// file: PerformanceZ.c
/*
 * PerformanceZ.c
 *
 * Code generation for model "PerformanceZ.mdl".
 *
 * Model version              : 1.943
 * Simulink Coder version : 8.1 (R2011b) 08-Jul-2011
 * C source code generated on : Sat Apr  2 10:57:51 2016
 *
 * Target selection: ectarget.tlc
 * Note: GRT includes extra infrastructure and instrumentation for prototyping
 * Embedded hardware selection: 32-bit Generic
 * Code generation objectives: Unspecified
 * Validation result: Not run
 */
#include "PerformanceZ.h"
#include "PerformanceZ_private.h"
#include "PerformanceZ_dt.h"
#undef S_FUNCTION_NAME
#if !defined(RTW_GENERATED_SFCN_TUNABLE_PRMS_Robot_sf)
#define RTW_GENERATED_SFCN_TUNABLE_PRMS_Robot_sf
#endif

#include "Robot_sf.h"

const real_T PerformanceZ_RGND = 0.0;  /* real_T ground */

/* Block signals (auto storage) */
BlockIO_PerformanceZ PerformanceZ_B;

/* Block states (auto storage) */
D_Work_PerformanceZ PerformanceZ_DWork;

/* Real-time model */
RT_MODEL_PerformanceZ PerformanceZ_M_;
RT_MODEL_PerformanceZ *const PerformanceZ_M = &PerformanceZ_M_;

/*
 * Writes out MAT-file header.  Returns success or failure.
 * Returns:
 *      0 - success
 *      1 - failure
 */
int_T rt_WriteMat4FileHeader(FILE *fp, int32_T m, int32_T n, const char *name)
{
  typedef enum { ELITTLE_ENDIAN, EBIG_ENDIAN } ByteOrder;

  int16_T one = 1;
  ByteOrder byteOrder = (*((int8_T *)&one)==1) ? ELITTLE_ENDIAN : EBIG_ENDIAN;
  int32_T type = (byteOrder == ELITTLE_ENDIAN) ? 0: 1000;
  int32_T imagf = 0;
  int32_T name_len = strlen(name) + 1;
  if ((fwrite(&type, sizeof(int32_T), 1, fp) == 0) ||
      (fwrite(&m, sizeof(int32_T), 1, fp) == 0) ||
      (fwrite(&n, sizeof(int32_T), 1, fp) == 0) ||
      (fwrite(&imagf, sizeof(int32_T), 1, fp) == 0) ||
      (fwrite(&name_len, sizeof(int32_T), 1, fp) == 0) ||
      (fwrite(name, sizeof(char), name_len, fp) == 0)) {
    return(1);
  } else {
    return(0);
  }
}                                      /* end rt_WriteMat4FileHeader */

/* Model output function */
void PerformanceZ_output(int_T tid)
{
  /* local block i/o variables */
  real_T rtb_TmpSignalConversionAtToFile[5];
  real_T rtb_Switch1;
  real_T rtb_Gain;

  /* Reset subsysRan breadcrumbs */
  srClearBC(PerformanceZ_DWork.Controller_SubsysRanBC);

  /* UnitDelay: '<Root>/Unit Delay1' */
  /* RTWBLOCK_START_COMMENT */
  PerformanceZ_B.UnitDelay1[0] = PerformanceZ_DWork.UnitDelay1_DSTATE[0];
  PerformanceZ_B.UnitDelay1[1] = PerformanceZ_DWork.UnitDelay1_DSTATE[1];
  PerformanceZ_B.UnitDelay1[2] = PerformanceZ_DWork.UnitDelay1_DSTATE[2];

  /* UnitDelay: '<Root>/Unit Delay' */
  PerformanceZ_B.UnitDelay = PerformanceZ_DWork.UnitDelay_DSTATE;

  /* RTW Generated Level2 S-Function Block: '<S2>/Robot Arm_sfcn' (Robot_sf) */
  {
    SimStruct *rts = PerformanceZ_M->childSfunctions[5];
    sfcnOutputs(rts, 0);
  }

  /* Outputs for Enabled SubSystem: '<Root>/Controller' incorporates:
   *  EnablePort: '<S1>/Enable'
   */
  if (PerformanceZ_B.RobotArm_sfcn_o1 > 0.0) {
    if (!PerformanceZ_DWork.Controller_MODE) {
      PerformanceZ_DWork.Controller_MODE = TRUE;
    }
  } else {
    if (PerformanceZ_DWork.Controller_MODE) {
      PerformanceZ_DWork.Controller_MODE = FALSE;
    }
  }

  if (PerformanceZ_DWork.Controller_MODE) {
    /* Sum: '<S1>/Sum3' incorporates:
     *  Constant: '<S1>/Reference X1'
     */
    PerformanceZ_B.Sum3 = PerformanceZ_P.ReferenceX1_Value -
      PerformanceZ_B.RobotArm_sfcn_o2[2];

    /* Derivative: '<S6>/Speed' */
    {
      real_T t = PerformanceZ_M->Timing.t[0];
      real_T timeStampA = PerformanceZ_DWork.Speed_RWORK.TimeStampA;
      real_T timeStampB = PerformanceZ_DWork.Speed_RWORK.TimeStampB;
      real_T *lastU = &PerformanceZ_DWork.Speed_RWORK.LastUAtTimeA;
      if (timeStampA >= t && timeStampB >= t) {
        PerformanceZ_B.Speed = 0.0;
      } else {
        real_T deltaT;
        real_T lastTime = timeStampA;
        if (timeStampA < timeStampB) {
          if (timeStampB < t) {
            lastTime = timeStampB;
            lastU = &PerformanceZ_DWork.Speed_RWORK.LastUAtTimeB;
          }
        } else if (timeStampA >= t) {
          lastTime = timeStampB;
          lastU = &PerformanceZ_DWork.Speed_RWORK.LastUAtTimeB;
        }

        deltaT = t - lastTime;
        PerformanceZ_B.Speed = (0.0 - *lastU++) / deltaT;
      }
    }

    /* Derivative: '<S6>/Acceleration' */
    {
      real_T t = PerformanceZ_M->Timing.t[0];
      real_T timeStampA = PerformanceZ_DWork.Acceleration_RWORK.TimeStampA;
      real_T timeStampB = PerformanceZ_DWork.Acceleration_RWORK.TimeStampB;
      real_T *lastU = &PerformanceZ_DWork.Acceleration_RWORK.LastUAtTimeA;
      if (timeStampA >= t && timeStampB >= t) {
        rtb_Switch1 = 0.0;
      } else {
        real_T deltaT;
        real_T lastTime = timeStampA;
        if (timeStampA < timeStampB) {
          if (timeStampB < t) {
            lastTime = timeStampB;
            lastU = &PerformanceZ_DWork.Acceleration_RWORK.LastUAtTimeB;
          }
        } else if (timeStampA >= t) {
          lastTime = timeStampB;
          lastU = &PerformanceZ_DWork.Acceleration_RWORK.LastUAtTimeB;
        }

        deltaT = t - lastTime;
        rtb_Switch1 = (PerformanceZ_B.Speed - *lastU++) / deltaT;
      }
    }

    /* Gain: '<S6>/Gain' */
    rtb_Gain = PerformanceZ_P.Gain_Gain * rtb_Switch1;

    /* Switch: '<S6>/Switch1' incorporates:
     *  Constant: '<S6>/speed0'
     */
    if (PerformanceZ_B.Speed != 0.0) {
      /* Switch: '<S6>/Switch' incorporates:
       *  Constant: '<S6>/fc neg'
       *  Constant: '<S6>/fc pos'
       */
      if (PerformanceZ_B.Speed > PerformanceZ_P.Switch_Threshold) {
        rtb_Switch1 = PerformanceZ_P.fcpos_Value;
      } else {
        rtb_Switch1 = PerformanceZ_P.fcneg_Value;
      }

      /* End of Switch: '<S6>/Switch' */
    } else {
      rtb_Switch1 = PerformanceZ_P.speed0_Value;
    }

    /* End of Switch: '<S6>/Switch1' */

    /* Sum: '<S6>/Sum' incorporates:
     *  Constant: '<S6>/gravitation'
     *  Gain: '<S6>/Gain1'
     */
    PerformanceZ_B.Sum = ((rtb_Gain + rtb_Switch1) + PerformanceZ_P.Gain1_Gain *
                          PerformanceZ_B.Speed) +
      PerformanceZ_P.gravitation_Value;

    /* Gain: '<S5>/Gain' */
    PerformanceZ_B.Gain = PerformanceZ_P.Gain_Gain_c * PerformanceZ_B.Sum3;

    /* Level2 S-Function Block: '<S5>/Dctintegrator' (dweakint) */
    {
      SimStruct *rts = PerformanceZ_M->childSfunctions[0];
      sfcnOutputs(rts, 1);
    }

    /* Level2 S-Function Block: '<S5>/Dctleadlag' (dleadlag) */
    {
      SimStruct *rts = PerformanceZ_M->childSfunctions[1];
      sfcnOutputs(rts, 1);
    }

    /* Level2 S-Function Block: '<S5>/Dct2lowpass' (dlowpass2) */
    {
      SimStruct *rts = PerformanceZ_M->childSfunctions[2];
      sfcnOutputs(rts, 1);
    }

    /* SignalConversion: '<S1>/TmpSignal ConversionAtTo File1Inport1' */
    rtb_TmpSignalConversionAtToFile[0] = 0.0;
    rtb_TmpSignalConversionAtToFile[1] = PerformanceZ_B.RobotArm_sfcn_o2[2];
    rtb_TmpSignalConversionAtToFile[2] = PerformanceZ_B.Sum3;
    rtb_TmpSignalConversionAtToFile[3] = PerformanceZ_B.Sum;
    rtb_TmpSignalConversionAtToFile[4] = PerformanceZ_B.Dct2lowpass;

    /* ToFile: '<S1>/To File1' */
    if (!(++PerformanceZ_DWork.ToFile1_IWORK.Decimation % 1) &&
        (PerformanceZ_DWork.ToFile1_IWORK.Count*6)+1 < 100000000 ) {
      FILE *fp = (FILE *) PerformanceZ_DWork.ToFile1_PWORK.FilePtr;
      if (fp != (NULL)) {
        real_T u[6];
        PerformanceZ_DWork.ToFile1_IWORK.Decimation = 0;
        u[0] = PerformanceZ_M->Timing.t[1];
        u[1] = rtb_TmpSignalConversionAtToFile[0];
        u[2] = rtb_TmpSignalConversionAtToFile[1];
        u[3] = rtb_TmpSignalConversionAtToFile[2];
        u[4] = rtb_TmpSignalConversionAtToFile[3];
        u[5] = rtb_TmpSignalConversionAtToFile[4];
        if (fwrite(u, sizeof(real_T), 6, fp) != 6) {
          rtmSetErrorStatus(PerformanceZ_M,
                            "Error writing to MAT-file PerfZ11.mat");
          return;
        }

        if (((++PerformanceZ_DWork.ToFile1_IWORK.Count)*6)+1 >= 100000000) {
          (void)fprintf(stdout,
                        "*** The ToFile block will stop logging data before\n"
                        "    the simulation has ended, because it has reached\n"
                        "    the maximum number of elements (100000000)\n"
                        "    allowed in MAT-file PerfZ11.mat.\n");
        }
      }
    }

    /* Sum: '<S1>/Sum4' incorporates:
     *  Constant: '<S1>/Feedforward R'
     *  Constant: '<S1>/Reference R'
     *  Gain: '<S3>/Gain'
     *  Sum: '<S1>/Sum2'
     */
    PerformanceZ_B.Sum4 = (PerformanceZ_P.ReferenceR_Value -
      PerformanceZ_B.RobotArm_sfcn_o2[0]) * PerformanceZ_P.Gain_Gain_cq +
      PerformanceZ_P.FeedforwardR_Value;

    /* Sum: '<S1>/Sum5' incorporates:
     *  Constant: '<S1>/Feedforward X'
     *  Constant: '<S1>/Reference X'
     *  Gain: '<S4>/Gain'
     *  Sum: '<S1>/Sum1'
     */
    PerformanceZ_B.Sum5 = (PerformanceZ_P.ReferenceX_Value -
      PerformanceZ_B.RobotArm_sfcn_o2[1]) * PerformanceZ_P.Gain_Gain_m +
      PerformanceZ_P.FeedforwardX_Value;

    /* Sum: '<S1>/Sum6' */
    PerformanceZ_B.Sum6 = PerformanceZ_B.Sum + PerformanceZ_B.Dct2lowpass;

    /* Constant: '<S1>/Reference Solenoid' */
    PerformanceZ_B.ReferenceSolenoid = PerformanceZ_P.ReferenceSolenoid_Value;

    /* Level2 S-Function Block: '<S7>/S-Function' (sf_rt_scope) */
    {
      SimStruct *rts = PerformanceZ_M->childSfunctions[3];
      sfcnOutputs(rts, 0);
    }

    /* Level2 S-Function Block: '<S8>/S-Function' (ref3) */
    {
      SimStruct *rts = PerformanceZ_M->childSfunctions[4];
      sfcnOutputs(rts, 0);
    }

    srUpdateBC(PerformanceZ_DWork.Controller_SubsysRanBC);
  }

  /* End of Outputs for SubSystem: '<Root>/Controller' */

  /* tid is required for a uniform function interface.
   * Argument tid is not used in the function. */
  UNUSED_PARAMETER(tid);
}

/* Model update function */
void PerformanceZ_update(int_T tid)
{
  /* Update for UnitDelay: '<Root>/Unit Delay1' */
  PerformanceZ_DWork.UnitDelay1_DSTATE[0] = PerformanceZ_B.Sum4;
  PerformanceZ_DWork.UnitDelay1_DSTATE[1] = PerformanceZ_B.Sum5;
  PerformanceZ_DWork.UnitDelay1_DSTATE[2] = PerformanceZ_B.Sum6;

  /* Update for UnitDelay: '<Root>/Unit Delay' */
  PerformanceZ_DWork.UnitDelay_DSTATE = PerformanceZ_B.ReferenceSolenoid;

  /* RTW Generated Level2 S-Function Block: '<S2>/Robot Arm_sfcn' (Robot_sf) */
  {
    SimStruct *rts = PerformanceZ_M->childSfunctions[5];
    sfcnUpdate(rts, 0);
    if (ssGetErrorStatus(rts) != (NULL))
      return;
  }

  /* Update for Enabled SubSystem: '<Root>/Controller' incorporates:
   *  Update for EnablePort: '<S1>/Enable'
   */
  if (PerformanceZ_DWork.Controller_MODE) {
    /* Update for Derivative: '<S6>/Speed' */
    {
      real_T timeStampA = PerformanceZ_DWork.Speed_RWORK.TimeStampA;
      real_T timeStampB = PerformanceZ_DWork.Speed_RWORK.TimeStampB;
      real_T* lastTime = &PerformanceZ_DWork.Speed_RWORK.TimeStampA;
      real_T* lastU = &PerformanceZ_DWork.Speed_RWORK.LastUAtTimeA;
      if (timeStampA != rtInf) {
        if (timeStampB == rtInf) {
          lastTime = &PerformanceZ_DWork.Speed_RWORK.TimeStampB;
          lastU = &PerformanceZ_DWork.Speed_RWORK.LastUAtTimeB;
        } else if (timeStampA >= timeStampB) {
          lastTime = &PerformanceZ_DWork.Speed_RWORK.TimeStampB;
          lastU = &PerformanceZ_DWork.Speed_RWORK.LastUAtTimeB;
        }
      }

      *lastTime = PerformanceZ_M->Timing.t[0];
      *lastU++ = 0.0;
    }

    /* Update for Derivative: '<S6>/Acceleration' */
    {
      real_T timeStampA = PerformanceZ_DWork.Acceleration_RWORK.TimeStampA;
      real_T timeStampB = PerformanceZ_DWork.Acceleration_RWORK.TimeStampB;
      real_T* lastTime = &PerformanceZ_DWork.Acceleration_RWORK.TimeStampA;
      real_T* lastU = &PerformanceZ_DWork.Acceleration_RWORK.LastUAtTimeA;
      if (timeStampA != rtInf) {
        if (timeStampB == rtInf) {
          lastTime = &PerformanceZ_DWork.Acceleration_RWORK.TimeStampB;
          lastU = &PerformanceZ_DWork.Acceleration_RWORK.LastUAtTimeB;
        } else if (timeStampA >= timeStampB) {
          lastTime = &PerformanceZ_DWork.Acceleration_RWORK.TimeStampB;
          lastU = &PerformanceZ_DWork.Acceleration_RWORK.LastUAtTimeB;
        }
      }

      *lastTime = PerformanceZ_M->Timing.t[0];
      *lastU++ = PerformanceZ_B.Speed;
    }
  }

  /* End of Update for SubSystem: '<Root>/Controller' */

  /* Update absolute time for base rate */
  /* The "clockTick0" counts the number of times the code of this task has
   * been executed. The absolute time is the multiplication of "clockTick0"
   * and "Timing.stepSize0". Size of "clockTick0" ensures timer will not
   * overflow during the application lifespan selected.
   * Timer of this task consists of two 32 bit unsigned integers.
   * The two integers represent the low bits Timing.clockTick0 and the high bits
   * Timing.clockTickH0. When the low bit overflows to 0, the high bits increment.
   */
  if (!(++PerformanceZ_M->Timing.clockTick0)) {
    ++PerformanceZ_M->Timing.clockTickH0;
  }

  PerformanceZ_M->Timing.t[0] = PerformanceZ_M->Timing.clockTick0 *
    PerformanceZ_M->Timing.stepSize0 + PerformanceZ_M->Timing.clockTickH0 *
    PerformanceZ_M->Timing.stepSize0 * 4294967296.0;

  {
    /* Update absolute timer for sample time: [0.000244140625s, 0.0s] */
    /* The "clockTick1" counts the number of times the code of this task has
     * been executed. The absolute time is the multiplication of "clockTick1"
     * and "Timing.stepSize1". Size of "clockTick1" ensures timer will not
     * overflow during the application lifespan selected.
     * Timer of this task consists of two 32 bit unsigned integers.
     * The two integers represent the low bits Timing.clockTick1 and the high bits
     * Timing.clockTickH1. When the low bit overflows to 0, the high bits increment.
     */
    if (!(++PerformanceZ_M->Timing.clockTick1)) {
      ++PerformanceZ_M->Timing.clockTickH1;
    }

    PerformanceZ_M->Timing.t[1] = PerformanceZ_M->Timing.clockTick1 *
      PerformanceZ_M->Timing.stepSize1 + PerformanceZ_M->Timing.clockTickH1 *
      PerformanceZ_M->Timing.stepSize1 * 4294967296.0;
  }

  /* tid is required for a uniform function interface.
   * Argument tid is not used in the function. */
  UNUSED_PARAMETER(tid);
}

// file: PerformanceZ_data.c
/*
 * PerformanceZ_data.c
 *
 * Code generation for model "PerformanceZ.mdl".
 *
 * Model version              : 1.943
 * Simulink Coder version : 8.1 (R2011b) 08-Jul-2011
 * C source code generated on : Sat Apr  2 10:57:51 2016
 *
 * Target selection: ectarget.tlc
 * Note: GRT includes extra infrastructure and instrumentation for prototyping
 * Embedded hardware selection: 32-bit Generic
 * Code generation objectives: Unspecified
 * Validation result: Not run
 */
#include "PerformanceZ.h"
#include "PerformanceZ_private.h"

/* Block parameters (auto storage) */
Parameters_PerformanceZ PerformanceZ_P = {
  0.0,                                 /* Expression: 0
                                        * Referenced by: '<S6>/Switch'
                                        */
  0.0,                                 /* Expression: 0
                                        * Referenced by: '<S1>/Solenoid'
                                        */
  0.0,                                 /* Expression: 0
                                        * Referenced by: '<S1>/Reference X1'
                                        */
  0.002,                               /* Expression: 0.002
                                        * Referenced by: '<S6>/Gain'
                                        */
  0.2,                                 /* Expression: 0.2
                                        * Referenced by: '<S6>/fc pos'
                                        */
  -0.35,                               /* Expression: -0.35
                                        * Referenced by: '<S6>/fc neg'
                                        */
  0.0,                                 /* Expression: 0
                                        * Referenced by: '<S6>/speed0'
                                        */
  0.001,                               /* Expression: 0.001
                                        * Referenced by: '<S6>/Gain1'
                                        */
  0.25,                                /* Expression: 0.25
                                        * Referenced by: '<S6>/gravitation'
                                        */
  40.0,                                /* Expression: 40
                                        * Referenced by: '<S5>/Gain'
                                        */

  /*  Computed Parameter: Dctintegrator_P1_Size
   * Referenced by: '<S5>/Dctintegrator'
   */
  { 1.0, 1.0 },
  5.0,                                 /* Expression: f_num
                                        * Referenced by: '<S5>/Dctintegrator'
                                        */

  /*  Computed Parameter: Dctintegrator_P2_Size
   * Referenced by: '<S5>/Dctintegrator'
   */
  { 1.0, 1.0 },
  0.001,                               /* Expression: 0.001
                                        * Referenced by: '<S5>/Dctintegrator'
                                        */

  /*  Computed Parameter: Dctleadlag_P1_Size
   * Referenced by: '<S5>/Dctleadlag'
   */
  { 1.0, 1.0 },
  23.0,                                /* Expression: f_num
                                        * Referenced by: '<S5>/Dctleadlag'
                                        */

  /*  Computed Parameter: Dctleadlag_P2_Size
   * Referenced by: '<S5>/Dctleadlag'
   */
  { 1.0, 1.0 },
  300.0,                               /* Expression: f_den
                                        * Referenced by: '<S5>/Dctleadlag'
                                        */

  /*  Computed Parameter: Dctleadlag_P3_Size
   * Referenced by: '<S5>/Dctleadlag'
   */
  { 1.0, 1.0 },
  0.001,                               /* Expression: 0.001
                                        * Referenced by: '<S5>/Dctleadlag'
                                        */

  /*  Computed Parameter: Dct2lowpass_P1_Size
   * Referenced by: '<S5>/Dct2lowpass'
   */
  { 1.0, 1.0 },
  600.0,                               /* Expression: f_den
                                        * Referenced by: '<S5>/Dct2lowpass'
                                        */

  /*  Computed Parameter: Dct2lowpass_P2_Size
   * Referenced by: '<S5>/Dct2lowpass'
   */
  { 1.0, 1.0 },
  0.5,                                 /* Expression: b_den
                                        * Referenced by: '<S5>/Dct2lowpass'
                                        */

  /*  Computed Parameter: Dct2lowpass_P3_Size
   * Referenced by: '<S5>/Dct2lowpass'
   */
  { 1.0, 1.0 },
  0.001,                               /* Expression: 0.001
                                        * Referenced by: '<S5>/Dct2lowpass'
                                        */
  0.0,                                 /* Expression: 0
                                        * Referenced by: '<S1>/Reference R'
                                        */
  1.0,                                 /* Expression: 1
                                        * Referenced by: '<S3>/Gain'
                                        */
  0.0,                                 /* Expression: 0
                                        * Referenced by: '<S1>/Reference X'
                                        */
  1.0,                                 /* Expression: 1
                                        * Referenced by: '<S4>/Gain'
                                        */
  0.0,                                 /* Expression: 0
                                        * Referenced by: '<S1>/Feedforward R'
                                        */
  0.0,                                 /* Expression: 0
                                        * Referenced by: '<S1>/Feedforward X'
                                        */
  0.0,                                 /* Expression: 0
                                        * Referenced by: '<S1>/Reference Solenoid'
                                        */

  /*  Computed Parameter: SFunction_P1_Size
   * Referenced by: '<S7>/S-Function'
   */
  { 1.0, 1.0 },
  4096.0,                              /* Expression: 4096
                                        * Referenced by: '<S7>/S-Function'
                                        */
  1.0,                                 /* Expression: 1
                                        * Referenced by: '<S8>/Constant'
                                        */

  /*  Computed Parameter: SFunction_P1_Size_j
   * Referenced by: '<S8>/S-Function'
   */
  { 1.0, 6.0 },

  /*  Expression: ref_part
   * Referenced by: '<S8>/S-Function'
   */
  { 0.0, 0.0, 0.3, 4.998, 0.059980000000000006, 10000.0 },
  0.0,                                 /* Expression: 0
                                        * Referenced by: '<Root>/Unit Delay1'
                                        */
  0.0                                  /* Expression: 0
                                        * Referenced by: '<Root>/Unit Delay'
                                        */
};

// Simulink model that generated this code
simulink model "PerformanceZ"  (Simulink 7.8)
settings: Solver=FixedStepDiscrete  StartTime=0.0  StopTime=20  FixedStep=1/(1024*4)  RelTol=1e-3

== system PerformanceZ ==
  Accelerometer : Display
  Controller : Subsystem
  Robot Arm : Subsystem
  Unit Delay : UnitDelay  SampleTime=-1
  Unit Delay1 : UnitDelay  SampleTime=-1
  time1 : Display
  wires:
  Controller/1(Output) -> Unit Delay1/1
  Robot Arm/1(Homing Busy) -> Controller/Enable
  Robot Arm/2(Angle measurments [rad]) -> Controller/1(Angle Measurements [rad])
  Robot Arm/3(Airbag Status) -> time1/1
  Robot Arm/4(Accelerometer [V]) -> Accelerometer/1
  Controller/2(Solenoid) -> Unit Delay/1
  Unit Delay/1 -> Robot Arm/2(Solenoid)
  Unit Delay1/1 -> Robot Arm/1(Input [V])

== system PerformanceZ/Controller ==
  Angle Measurements [rad] : Inport
  Enable : EnablePort
  Bus Creator : BusCreator  Inputs=5
  Controller R : Subsystem
  Controller X : Subsystem
  Controller Z : Subsystem
  Demux : Demux  Outputs=3
  Feedforward R : Constant  Value=0
  Feedforward X : Constant  Value=0
  Feedforward Z : Subsystem
  Mux : Mux  Inputs=3
  RTScope : Subsystem
  Reference R : Constant  Value=0
  Reference Solenoid : Constant  Value=0
  Reference X : Constant  Value=0
  Step : Step  After=-0.22
  Subsystem : Subsystem
  Sum1 : Sum  Inputs=|+-
  Sum2 : Sum  Inputs=|+-
  Sum3 : Sum  Inputs=|+-
  Sum4 : Sum  Inputs=++|  SaturateOnIntegerOverflow=on  InputSameDT=on  OutDataTypeStr=Inherit: Same as first input
  Sum5 : Sum  Inputs=++|  SaturateOnIntegerOverflow=on  InputSameDT=on  OutDataTypeStr=Inherit: Same as first input
  Sum6 : Sum  Inputs=++|  SaturateOnIntegerOverflow=on  InputSameDT=on  OutDataTypeStr=Inherit: Same as first input
  To File1 : ToFile  Filename=PerfZ11.mat  MatrixName=signals
  time2 : Display
  Output : Outport
  Solenoid : Outport  Port=2  InitialOutput=0
  wires:
  Mux/1 -> Output/1
  Angle Measurements [rad]/1 -> Demux/1
  Demux/1 -> Sum2/2  "R"
  Demux/2 -> Sum1/2  "X"
  Demux/3 -> Sum3/2, time2/1, Bus Creator/2  "Z"
  Sum4/1 -> Mux/1
  Sum5/1 -> Mux/2
  Sum6/1 -> Mux/3
  Reference Solenoid/1 -> Solenoid/1
  Bus Creator/1 -> To File1/1
  Feedforward R/1 -> Sum4/1
  Reference R/1 -> Sum2/1
  Controller R/1(Output) -> Sum4/2
  Sum2/1 -> Controller R/1(Input)
  Feedforward X/1 -> Sum5/1
  Controller X/1(Output) -> Sum5/2
  Controller Z/1(Output) -> Sum6/2, Bus Creator/5
  Sum1/1 -> Controller X/1(Input)
  Sum3/1 -> Controller Z/1(Input), Bus Creator/3
  Reference X/1 -> Sum1/1
  Feedforward Z/1(Out1) -> Sum6/1, Bus Creator/4
  Step/1 -> Sum3/1, Feedforward Z/1(In1), Bus Creator/1

== system PerformanceZ/Robot Arm ==
  Input [V] : Inport
  Solenoid : Inport  Port=2
  Robot Arm_sfcn : S-Function  FunctionName=Robot_sf  SFunctionModules=ec_Ebox dweakint dpd dnotch dlowpass2 ec_EboxResetEnc  EnableBusSupport=off  mask{rtw_sf_name=Robot_sf, showVar=off}
      mask prompts: rtw_sf_name "Generated S-function name (model_sf):"; showVar "Show module list"
      mask help: Simulink Coder generated S-function.
      mask init:
      | displist = '';
      | if ~strcmp(get_param(gcb, 'FunctionName'), rtw_sf_name);
      |   set_param(gcb, 'FunctionName', rtw_sf_name);
      | end
      | % Check if we are generating code
      | rtw_mode = false;
      | if strcmpi(get_param(bdroot(gcb),'SimulationStatus'),'Initializing')
      | 	rtw_mode = strcmpi(get_param(bdroot(gcb),'BuildingRTWCode'),'on') && ...
      | 		~strcmpi(get_param(bdroot(gcb),'TargetStyle'),'SimulationTarget');
      | end
      | if showVar || rtw_mode
      | 	if exist('rtwsfunc') == 2 | exist('rtwsfunc') == 6
      | 		tmplist = rtwsfunc(rtw_sf_name,gcb);
      | 		tmplist = ['\nList of Modules:\n', tmplist];
      | 	elseif showVar
      | 		tmplist = '\nList of Modules:\nNot licensed\n';
      |  	end
      | end
      | if showVar
      |   displist = tmplist;
      | end
  __InputSSForSFun__ : Subsystem
  __OutputSSForSFun__ : Subsystem
  Homing Busy : Outport
  Angle measurments [rad] : Outport  Port=2
  Airbag Status : Outport  Port=3
  Accelerometer [V] : Outport  Port=4
  wires:
  Input [V]/1 -> __InputSSForSFun__/1(Input [V])
  Solenoid/1 -> __InputSSForSFun__/2(Solenoid)
  __InputSSForSFun__/1(__UniqueOutportName__1__) -> Robot Arm_sfcn/1
  __InputSSForSFun__/2(__UniqueOutportName__2__) -> Robot Arm_sfcn/2
  Robot Arm_sfcn/1 -> __OutputSSForSFun__/1(__UniqueInportName__1__)
  Robot Arm_sfcn/2 -> __OutputSSForSFun__/2(__UniqueInportName__2__)
  Robot Arm_sfcn/3 -> __OutputSSForSFun__/3(__UniqueInportName__3__)
  Robot Arm_sfcn/4 -> __OutputSSForSFun__/4(__UniqueInportName__4__)
  __OutputSSForSFun__/1(Homing Busy) -> Homing Busy/1
  __OutputSSForSFun__/2(Angle measurments [rad]) -> Angle measurments [rad]/1
  __OutputSSForSFun__/3(Airbag Status) -> Airbag Status/1
  __OutputSSForSFun__/4(Accelerometer [V]) -> Accelerometer [V]/1

== system PerformanceZ/Controller/Controller R ==
  Input : Inport
  Gain : Gain
  Output : Outport
  wires:
  Input/1 -> Gain/1
  Gain/1 -> Output/1

== system PerformanceZ/Controller/Controller X ==
  Input : Inport
  Gain : Gain
  Output : Outport
  wires:
  Input/1 -> Gain/1
  Gain/1 -> Output/1

== system PerformanceZ/Controller/Controller Z ==
  Input : Inport
  Dct2lowpass : S-Function  FunctionName=dlowpass2  Parameters=f_den, b_den, 0.001  EnableBusSupport=off  mask(dctools){f_den=600, b_den=0.5}
      mask prompts: f_den "Pole [Hz]"; b_den "Damping pole [-]"
      mask help: This block implements a discrete time 2nd order lowpass filter.
  Dctintegrator : S-Function  FunctionName=dweakint  Parameters=f_num, 0.001  EnableBusSupport=off  mask(dctools){f_num=5}
      mask prompts: f_num "Zero [Hz]"
      mask help: This block implements a discrete time weak integrator filter.
  Dctleadlag : S-Function  FunctionName=dleadlag  Parameters=f_num, f_den, 0.001  EnableBusSupport=off  mask(dctools){f_num=23, f_den=300}
      mask prompts: f_num "Zero [Hz]"; f_den "Pole [Hz]"
      mask help: This block implements a discrete time leadlag filter.
  Gain : Gain  Gain=40
  Output : Outport
  wires:
  Input/1 -> Gain/1
  Gain/1 -> Dctintegrator/1
  Dctintegrator/1 -> Dctleadlag/1
  Dctleadlag/1 -> Dct2lowpass/1
  Dct2lowpass/1 -> Output/1

== system PerformanceZ/Controller/Feedforward Z ==
  In1 : Inport
  Acceleration : Derivative
  Gain : Gain  Gain=0.002
  Gain1 : Gain  Gain=0.001
  Speed : Derivative
  Sum : Sum  Inputs=+|+|+|+
  Switch : Switch  Criteria=u2 > Threshold
  Switch1 : Switch  Criteria=u2 ~= 0
  fc neg : Constant  Value=-0.35
  fc pos : Constant  Value=0.2
  gravitation : Constant  Value=0.25
  speed0 : Constant  Value=0
  Out1 : Outport
  wires:
  Switch1/1 -> Sum/2
  speed0/1 -> Switch1/3
  Switch/1 -> Switch1/1
  fc neg/1 -> Switch/3
  fc pos/1 -> Switch/1
  Gain1/1 -> Sum/3
  Gain/1 -> Sum/1
  Sum/1 -> Out1/1
  Speed/1 -> Gain1/1, Switch1/2, Switch/2, Acceleration/1
  Acceleration/1 -> Gain/1
  In1/1 -> Speed/1
  gravitation/1 -> Sum/4

== system PerformanceZ/Controller/RTScope ==
  In1 : Inport
  In2 : Inport  Port=2
  In3 : Inport  Port=3
  In4 : Inport  Port=4
  In5 : Inport  Port=5
  In6 : Inport  Port=6
  In7 : Inport  Port=7
  In8 : Inport  Port=8
  Demux : Demux
  Mux : Mux  Inputs=8
  S-Function : S-Function  FunctionName=sf_rt_scope  Parameters=4096  EnableBusSupport=off
  Out1 : Outport
  Out2 : Outport  Port=2
  Out3 : Outport  Port=3
  Out4 : Outport  Port=4
  wires:
  In8/1 -> Mux/8
  In7/1 -> Mux/7
  In6/1 -> Mux/6
  In5/1 -> Mux/5
  In4/1 -> Mux/4
  In3/1 -> Mux/3
  In2/1 -> Mux/2
  In1/1 -> Mux/1
  Demux/4 -> Out4/1
  Demux/3 -> Out3/1
  Demux/2 -> Out2/1
  Demux/1 -> Out1/1
  S-Function/1 -> Demux/1
  Mux/1 -> S-Function/1

== system PerformanceZ/Controller/Subsystem ==
  Constant : Constant
  Demux : Demux  Outputs=3
  S-Function : S-Function  FunctionName=ref3  Parameters=ref_part  EnableBusSupport=off
  acc : Outport
  vel : Outport  Port=2
  pos : Outport  Port=3
  wires:
  Constant/1 -> S-Function/1
  S-Function/1 -> Demux/1
  Demux/1 -> acc/1
  Demux/2 -> vel/1
  Demux/3 -> pos/1

== system PerformanceZ/Robot Arm/__InputSSForSFun__ ==
  Input [V] : Inport
  Solenoid : Inport  Port=2
  __UniqueOutportName__1__ : Outport
  __UniqueOutportName__2__ : Outport  Port=2
  wires:
  Input [V]/1 -> __UniqueOutportName__1__/1
  Solenoid/1 -> __UniqueOutportName__2__/1

== system PerformanceZ/Robot Arm/__OutputSSForSFun__ ==
  __UniqueInportName__1__ : Inport
  __UniqueInportName__2__ : Inport  Port=2
  __UniqueInportName__3__ : Inport  Port=3
  __UniqueInportName__4__ : Inport  Port=4
  Homing Busy : Outport
  Angle measurments [rad] : Outport  Port=2
  Airbag Status : Outport  Port=3
  Accelerometer [V] : Outport  Port=4
  wires:
  __UniqueInportName__1__/1 -> Homing Busy/1
  __UniqueInportName__2__/1 -> Angle measurments [rad]/1
  __UniqueInportName__3__/1 -> Airbag Status/1
  __UniqueInportName__4__/1 -> Accelerometer [V]/1
